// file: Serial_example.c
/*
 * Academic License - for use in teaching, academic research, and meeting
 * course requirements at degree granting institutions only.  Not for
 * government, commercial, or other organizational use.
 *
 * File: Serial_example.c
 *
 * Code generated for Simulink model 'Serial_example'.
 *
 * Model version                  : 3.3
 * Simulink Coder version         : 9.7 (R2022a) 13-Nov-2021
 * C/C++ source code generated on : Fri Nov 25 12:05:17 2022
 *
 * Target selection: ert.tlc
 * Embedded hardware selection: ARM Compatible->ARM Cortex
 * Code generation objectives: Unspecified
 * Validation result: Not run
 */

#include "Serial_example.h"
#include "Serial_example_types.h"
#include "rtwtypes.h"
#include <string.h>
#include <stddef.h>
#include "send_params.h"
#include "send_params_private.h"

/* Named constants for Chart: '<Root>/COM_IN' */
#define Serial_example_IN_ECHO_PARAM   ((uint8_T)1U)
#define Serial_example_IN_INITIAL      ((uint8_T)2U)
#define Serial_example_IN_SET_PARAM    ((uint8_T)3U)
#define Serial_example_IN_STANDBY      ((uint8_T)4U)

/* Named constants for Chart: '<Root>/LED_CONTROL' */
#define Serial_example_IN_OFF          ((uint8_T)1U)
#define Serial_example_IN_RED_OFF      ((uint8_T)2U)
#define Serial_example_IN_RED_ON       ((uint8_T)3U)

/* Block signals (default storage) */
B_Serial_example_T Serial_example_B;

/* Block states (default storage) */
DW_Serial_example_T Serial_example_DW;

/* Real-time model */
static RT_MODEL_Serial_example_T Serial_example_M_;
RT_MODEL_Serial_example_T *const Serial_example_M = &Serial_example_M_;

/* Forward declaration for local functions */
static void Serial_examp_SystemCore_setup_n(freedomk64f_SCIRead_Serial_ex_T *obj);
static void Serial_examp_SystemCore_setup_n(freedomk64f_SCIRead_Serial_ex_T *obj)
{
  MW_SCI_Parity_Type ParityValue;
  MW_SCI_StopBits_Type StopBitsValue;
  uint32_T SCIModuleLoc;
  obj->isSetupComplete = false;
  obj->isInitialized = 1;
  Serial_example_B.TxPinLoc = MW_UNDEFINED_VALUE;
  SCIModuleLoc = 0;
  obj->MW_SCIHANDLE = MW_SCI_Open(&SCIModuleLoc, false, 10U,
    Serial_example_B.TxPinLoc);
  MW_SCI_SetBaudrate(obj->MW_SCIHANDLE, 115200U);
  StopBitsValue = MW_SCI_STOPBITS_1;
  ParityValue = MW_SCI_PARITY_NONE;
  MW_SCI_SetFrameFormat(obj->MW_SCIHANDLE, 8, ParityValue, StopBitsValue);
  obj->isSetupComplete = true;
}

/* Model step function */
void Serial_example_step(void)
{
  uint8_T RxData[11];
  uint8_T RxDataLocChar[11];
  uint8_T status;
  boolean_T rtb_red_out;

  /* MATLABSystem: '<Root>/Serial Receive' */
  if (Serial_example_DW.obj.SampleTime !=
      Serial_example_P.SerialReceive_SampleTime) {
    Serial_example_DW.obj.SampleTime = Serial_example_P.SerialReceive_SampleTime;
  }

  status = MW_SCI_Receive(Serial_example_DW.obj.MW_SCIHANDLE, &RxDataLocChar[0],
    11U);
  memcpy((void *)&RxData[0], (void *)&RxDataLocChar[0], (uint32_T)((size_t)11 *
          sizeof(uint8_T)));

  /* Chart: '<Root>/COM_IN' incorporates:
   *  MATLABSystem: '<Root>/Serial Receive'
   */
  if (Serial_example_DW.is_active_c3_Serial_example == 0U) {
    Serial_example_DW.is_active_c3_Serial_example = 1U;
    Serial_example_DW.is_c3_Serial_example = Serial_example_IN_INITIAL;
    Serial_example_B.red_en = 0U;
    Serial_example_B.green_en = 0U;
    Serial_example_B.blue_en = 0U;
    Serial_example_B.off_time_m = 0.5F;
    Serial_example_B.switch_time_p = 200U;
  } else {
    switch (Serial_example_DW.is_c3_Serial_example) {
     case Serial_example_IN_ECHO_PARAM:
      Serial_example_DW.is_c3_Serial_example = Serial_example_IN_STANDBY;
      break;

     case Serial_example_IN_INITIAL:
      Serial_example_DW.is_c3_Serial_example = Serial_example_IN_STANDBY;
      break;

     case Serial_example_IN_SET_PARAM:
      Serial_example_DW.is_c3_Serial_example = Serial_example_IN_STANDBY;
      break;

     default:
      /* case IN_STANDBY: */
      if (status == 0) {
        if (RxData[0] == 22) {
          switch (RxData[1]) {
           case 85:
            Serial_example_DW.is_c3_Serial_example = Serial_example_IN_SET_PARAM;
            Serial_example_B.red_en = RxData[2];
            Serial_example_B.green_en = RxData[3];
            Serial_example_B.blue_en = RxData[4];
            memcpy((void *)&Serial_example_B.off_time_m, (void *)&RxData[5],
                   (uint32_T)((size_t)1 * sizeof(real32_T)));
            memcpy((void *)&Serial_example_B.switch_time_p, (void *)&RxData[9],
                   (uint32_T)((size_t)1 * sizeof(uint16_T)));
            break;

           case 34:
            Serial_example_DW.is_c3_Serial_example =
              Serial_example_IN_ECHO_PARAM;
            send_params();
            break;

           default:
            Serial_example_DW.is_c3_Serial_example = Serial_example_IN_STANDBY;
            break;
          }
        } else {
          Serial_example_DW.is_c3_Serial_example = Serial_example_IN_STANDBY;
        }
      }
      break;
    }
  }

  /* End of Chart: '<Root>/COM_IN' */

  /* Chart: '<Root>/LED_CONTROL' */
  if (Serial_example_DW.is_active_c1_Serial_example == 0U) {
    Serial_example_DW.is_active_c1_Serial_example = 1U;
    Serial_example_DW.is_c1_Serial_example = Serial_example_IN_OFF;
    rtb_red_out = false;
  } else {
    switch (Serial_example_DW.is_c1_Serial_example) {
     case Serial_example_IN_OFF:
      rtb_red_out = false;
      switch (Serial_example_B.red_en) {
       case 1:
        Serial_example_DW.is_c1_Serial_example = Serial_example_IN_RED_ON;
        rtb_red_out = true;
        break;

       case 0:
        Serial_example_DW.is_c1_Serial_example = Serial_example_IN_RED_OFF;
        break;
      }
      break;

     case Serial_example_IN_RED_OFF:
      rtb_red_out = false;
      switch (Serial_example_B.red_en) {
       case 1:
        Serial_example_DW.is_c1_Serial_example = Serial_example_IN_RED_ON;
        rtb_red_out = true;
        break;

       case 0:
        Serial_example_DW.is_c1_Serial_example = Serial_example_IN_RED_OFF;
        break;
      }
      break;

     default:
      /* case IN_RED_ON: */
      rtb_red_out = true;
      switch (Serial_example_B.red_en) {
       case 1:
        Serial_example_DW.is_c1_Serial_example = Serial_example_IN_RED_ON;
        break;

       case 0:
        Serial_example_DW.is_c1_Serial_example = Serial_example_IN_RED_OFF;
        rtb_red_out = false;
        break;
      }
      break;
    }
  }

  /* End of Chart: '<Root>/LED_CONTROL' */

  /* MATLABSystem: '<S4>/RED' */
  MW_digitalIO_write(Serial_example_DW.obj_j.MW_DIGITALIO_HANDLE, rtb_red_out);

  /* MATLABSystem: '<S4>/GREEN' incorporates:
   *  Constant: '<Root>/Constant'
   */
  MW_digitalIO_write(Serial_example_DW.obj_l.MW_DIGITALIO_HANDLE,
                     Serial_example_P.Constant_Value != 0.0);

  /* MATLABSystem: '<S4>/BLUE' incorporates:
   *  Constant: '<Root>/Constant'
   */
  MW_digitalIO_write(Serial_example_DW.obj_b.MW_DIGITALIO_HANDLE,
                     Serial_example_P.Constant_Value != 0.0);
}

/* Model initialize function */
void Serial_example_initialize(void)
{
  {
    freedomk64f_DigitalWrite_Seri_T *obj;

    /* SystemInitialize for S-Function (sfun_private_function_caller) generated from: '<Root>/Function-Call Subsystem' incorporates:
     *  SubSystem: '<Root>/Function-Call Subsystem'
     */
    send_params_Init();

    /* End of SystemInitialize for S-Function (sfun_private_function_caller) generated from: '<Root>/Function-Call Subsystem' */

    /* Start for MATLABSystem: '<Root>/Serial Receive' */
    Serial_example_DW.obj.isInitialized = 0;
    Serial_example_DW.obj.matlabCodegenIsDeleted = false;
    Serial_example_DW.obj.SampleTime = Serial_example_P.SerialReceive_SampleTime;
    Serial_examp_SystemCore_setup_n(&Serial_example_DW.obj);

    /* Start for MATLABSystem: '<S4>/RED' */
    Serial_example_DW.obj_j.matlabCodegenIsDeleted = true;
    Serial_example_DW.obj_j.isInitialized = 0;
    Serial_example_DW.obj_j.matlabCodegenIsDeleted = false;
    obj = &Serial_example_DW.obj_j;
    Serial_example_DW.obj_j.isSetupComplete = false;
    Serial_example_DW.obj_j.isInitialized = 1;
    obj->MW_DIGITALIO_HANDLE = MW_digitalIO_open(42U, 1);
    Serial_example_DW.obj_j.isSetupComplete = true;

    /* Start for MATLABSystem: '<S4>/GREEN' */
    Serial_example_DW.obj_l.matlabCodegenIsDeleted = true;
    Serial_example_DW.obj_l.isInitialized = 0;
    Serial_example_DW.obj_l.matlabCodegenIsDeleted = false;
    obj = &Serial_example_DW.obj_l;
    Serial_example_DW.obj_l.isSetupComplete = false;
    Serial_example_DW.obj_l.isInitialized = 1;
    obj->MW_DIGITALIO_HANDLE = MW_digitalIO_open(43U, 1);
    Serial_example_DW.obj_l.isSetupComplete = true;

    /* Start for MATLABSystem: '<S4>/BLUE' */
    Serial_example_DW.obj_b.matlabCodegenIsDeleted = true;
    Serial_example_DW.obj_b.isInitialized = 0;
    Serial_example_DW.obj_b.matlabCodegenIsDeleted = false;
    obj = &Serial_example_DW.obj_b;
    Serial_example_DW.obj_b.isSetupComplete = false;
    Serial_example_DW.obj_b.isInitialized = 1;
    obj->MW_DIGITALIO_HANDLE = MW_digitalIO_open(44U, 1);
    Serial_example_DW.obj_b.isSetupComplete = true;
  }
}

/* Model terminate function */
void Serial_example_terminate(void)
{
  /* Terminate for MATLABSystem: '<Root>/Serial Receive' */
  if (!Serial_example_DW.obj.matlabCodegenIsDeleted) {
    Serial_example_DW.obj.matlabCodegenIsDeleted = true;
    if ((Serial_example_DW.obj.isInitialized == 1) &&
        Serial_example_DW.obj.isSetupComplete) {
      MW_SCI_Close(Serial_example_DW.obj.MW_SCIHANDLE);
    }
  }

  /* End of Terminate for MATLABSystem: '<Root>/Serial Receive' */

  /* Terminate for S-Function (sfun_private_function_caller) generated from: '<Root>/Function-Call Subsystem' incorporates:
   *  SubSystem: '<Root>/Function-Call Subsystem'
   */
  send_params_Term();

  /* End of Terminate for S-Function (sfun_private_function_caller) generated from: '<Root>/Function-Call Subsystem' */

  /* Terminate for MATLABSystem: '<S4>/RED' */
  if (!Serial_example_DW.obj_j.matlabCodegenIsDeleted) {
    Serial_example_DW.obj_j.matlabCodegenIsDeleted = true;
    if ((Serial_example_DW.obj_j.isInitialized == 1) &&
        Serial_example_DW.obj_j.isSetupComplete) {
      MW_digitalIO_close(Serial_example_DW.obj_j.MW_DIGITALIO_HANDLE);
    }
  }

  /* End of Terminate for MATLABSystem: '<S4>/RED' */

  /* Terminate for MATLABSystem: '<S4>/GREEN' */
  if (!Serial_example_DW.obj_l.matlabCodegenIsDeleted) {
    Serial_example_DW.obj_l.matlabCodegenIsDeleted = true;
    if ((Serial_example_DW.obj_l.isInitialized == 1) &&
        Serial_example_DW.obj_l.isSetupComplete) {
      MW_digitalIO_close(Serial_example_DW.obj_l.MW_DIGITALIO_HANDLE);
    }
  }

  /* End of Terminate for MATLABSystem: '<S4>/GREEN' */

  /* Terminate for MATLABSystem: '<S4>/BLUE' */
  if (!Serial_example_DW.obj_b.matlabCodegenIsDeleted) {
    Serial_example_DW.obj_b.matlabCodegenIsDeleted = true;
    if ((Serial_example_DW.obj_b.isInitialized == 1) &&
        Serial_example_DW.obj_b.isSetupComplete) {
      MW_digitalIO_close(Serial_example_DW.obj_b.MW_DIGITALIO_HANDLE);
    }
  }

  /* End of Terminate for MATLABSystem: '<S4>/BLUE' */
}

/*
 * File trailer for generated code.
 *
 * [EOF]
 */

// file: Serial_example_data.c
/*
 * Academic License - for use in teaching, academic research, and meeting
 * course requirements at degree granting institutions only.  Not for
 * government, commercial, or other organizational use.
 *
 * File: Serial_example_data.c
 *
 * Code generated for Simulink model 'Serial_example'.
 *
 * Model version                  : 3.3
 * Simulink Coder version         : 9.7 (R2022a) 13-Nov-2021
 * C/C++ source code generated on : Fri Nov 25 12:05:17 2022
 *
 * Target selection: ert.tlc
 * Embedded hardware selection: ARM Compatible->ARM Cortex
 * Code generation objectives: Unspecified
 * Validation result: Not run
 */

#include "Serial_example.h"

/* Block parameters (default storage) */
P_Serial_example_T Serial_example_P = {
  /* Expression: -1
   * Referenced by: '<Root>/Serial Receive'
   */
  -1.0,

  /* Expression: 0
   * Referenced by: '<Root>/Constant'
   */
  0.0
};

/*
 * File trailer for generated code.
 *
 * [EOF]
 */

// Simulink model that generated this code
simulink model "Serial_example"  (R2022a)
settings: Solver=FixedStepAuto  StartTime=0.0  StopTime=10.0  FixedStep=1e-3  RelTol=1e-3  EnableMultiTasking=on
libraries: frdmk64flib x5, etargetslib x2

== system Serial_example ==
  COM_IN : Stateflow chart  TreatAsAtomicUnit=on
  Constant : Constant  Value=0
  Function-Call Subsystem : Subsystem  TreatAsAtomicUnit=on
  LED_CONTROL : Stateflow chart  TreatAsAtomicUnit=on
  Serial Receive : frdmk64flib/Serial Receive  SCIModule=0  Baudrate=uint32(9600)  Parity=None  StopBits=1  HardwareFlowControl=None  ByteOrder=LittleEndian  DataType=uint8  DataLength=11  BlockingMode=off  OutputStatus=on  SampleTime=-1
  Subsystem : Subsystem
  wires:
  Serial Receive/1 -> COM_IN/1(rxdata)
  Serial Receive/2 -> COM_IN/2(status)
  LED_CONTROL/1(red_out) -> Subsystem/1(red_led)
  COM_IN/5(switch_time) -> Function-Call Subsystem/5(switch_time), LED_CONTROL/5(switch_time)
  COM_IN/1(red_en) -> Function-Call Subsystem/1(red_en), LED_CONTROL/1(red_en)
  COM_IN/4(off_time) -> Function-Call Subsystem/4(off_time), LED_CONTROL/4(off_time)
  COM_IN/2(green_en) -> Function-Call Subsystem/2(green_en), LED_CONTROL/2(green_en)
  COM_IN/3(blue_en) -> Function-Call Subsystem/3(blue_en), LED_CONTROL/3(blue_en)
  Constant/1 -> Subsystem/3(blue_led), Subsystem/2(green_led)

== system Serial_example/Function-Call Subsystem ==
  red_en : Inport
  green_en : Inport  Port=2
  blue_en : Inport  Port=3
  off_time : Inport  Port=4
  switch_time : Inport  Port=5
  function : TriggerPort  TriggerType=function-call  IsSimulinkFunction=on  FunctionName=send_params  VariantControl=(inherit)
  Byte Pack : etargetslib/Byte Pack  datatypes={'single'}  byteAlign=1
  Byte Pack1 : etargetslib/Byte Pack  datatypes={'uint16'}  byteAlign=1
  Mux : Mux  Inputs=5
  Serial Transmit : frdmk64flib/Serial Transmit  SCIModule=0  Baudrate=uint32(9600)  Parity=None  StopBits=1  HardwareFlowControl=None  ByteOrder=LittleEndian  BlockingMode=on  OutputStatus=off
  wires:
  off_time/1 -> Byte Pack/1
  switch_time/1 -> Byte Pack1/1
  Mux/1 -> Serial Transmit/1
  red_en/1 -> Mux/1
  green_en/1 -> Mux/2
  blue_en/1 -> Mux/3
  Byte Pack/1 -> Mux/4
  Byte Pack1/1 -> Mux/5

== system Serial_example/Subsystem ==
  red_led : Inport
  green_led : Inport  Port=2
  blue_led : Inport  Port=3
  BLUE : frdmk64flib/Digital Write  Whichpin=BLUE_LED
  GREEN : frdmk64flib/Digital Write  Whichpin=GREEN_LED
  RED : frdmk64flib/Digital Write  Whichpin=RED_LED
  wires:
  blue_led/1 -> BLUE/1
  red_led/1 -> RED/1
  green_led/1 -> GREEN/1

== stateflow chart Serial_example/LED_CONTROL ==
  state RED_OFF
    entry:
    red_out=false;
  state OFF
    entry:
    red_out=false;
  state RED_ON
    entry:
    red_out=true;
  RED_OFF -> (junction 14)
  (junction 14) -> RED_OFF [order 2] : [red_en==0]
  (default) -> OFF
  OFF -> (junction 14) : after(off_time,sec)
  (junction 14) -> RED_ON [order 1] : [red_en==1]
  RED_ON -> (junction 14)
  data: red_en input uint8; green_en input uint8; blue_en input uint8; off_time input single; red_out output boolean; switch_time input uint16

== stateflow chart Serial_example/COM_IN ==
  state SET_PARAM
    entry:
    red_en = rxdata(3);
    green_en =  rxdata(4);
    blue_en = rxdata(5);
    off_time = typecast(rxdata(6:9), 'sinlge');
    switch_time = typecast(rxdata(10:11), 'uint16');
  state INITIAL
    entry:
    red_en = 0;
    green_en = 0;
    blue_en = 0;
    off_time = 0.5;
    switch_time = 200;
  state STANDBY
  state ECHO_PARAM
    entry:
    send_params();
  SET_PARAM -> STANDBY
  (junction 15) -> SET_PARAM [order 1] : [rxdata(2)==hex2dec('55')]
  (default) -> INITIAL
  (junction 14) -> STANDBY [order 2]
  INITIAL -> STANDBY
  STANDBY -> (junction 14) : [status==0]
  (junction 14) -> (junction 15) [order 1] : [rxdata(1)==hex2dec('16')]
  (junction 15) -> ECHO_PARAM [order 2] : [rxdata(2)==hex2dec('22')]
  ECHO_PARAM -> STANDBY
  data: rxdata input uint8; status input uint8; red_en output uint8; green_en output uint8; blue_en output uint8; off_time output single; switch_time output uint16
